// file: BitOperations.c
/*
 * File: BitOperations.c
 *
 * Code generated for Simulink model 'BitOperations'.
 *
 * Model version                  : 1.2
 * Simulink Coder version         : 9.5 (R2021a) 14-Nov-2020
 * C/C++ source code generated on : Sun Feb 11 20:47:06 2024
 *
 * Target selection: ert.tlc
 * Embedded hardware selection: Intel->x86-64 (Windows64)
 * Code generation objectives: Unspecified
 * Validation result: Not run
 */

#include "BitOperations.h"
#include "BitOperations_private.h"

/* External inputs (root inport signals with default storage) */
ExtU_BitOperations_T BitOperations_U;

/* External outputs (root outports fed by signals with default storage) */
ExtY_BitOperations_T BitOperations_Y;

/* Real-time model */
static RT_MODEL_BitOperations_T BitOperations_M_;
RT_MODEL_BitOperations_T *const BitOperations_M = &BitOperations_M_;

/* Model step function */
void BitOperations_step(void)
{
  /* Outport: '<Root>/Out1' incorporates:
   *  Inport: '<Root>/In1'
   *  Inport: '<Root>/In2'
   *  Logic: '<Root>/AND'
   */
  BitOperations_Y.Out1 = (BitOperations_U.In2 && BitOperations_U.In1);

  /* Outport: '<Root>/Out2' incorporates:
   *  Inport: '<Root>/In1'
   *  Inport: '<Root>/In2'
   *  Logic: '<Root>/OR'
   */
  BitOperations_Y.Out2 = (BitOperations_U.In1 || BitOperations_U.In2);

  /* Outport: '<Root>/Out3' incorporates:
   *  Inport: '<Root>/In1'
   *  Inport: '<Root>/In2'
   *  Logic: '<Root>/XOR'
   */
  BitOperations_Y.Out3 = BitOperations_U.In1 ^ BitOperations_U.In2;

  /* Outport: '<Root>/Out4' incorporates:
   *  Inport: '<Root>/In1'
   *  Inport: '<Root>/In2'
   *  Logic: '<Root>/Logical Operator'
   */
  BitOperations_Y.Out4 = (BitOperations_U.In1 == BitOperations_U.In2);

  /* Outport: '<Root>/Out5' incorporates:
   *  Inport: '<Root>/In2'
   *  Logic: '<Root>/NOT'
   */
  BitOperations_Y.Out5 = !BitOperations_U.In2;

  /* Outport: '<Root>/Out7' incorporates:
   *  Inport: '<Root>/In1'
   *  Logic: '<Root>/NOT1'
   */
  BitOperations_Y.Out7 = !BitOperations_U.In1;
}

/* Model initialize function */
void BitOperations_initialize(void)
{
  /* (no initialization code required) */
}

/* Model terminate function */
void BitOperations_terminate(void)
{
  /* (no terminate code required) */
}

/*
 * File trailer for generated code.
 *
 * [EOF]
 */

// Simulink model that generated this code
simulink model "BitOperations"  (R2021a)
settings: Solver=FixedStepDiscrete  StartTime=0.0  StopTime=10.0  RelTol=1e-3

== system BitOperations ==
  In1 : Inport  OutDataTypeStr=boolean
  In2 : Inport  Port=2
  AND : Logic  IconShape=distinctive  AllPortsSameDT=off  OutDataTypeStr=boolean
  Logical Operator : Logic  Operator=NXOR  AllPortsSameDT=off  OutDataTypeStr=boolean
  NOT : Logic  Operator=NOT  IconShape=distinctive  AllPortsSameDT=off  OutDataTypeStr=boolean
  NOT1 : Logic  Operator=NOT  IconShape=distinctive  AllPortsSameDT=off  OutDataTypeStr=boolean
  OR : Logic  Operator=OR  IconShape=distinctive  AllPortsSameDT=off  OutDataTypeStr=boolean
  XOR : Logic  Operator=XOR  IconShape=distinctive  AllPortsSameDT=off  OutDataTypeStr=boolean
  Out1 : Outport
  Out2 : Outport  Port=2
  Out3 : Outport  Port=3
  Out4 : Outport  Port=4
  Out5 : Outport  Port=5
  Out7 : Outport  Port=6
  wires:
  In1/1 -> NOT1/1, Logical Operator/1, XOR/1, OR/1, AND/2
  In2/1 -> NOT/1, Logical Operator/2, XOR/2, OR/2, AND/1
  AND/1 -> Out1/1
  OR/1 -> Out2/1
  XOR/1 -> Out3/1
  Logical Operator/1 -> Out4/1
  NOT/1 -> Out5/1
  NOT1/1 -> Out7/1
